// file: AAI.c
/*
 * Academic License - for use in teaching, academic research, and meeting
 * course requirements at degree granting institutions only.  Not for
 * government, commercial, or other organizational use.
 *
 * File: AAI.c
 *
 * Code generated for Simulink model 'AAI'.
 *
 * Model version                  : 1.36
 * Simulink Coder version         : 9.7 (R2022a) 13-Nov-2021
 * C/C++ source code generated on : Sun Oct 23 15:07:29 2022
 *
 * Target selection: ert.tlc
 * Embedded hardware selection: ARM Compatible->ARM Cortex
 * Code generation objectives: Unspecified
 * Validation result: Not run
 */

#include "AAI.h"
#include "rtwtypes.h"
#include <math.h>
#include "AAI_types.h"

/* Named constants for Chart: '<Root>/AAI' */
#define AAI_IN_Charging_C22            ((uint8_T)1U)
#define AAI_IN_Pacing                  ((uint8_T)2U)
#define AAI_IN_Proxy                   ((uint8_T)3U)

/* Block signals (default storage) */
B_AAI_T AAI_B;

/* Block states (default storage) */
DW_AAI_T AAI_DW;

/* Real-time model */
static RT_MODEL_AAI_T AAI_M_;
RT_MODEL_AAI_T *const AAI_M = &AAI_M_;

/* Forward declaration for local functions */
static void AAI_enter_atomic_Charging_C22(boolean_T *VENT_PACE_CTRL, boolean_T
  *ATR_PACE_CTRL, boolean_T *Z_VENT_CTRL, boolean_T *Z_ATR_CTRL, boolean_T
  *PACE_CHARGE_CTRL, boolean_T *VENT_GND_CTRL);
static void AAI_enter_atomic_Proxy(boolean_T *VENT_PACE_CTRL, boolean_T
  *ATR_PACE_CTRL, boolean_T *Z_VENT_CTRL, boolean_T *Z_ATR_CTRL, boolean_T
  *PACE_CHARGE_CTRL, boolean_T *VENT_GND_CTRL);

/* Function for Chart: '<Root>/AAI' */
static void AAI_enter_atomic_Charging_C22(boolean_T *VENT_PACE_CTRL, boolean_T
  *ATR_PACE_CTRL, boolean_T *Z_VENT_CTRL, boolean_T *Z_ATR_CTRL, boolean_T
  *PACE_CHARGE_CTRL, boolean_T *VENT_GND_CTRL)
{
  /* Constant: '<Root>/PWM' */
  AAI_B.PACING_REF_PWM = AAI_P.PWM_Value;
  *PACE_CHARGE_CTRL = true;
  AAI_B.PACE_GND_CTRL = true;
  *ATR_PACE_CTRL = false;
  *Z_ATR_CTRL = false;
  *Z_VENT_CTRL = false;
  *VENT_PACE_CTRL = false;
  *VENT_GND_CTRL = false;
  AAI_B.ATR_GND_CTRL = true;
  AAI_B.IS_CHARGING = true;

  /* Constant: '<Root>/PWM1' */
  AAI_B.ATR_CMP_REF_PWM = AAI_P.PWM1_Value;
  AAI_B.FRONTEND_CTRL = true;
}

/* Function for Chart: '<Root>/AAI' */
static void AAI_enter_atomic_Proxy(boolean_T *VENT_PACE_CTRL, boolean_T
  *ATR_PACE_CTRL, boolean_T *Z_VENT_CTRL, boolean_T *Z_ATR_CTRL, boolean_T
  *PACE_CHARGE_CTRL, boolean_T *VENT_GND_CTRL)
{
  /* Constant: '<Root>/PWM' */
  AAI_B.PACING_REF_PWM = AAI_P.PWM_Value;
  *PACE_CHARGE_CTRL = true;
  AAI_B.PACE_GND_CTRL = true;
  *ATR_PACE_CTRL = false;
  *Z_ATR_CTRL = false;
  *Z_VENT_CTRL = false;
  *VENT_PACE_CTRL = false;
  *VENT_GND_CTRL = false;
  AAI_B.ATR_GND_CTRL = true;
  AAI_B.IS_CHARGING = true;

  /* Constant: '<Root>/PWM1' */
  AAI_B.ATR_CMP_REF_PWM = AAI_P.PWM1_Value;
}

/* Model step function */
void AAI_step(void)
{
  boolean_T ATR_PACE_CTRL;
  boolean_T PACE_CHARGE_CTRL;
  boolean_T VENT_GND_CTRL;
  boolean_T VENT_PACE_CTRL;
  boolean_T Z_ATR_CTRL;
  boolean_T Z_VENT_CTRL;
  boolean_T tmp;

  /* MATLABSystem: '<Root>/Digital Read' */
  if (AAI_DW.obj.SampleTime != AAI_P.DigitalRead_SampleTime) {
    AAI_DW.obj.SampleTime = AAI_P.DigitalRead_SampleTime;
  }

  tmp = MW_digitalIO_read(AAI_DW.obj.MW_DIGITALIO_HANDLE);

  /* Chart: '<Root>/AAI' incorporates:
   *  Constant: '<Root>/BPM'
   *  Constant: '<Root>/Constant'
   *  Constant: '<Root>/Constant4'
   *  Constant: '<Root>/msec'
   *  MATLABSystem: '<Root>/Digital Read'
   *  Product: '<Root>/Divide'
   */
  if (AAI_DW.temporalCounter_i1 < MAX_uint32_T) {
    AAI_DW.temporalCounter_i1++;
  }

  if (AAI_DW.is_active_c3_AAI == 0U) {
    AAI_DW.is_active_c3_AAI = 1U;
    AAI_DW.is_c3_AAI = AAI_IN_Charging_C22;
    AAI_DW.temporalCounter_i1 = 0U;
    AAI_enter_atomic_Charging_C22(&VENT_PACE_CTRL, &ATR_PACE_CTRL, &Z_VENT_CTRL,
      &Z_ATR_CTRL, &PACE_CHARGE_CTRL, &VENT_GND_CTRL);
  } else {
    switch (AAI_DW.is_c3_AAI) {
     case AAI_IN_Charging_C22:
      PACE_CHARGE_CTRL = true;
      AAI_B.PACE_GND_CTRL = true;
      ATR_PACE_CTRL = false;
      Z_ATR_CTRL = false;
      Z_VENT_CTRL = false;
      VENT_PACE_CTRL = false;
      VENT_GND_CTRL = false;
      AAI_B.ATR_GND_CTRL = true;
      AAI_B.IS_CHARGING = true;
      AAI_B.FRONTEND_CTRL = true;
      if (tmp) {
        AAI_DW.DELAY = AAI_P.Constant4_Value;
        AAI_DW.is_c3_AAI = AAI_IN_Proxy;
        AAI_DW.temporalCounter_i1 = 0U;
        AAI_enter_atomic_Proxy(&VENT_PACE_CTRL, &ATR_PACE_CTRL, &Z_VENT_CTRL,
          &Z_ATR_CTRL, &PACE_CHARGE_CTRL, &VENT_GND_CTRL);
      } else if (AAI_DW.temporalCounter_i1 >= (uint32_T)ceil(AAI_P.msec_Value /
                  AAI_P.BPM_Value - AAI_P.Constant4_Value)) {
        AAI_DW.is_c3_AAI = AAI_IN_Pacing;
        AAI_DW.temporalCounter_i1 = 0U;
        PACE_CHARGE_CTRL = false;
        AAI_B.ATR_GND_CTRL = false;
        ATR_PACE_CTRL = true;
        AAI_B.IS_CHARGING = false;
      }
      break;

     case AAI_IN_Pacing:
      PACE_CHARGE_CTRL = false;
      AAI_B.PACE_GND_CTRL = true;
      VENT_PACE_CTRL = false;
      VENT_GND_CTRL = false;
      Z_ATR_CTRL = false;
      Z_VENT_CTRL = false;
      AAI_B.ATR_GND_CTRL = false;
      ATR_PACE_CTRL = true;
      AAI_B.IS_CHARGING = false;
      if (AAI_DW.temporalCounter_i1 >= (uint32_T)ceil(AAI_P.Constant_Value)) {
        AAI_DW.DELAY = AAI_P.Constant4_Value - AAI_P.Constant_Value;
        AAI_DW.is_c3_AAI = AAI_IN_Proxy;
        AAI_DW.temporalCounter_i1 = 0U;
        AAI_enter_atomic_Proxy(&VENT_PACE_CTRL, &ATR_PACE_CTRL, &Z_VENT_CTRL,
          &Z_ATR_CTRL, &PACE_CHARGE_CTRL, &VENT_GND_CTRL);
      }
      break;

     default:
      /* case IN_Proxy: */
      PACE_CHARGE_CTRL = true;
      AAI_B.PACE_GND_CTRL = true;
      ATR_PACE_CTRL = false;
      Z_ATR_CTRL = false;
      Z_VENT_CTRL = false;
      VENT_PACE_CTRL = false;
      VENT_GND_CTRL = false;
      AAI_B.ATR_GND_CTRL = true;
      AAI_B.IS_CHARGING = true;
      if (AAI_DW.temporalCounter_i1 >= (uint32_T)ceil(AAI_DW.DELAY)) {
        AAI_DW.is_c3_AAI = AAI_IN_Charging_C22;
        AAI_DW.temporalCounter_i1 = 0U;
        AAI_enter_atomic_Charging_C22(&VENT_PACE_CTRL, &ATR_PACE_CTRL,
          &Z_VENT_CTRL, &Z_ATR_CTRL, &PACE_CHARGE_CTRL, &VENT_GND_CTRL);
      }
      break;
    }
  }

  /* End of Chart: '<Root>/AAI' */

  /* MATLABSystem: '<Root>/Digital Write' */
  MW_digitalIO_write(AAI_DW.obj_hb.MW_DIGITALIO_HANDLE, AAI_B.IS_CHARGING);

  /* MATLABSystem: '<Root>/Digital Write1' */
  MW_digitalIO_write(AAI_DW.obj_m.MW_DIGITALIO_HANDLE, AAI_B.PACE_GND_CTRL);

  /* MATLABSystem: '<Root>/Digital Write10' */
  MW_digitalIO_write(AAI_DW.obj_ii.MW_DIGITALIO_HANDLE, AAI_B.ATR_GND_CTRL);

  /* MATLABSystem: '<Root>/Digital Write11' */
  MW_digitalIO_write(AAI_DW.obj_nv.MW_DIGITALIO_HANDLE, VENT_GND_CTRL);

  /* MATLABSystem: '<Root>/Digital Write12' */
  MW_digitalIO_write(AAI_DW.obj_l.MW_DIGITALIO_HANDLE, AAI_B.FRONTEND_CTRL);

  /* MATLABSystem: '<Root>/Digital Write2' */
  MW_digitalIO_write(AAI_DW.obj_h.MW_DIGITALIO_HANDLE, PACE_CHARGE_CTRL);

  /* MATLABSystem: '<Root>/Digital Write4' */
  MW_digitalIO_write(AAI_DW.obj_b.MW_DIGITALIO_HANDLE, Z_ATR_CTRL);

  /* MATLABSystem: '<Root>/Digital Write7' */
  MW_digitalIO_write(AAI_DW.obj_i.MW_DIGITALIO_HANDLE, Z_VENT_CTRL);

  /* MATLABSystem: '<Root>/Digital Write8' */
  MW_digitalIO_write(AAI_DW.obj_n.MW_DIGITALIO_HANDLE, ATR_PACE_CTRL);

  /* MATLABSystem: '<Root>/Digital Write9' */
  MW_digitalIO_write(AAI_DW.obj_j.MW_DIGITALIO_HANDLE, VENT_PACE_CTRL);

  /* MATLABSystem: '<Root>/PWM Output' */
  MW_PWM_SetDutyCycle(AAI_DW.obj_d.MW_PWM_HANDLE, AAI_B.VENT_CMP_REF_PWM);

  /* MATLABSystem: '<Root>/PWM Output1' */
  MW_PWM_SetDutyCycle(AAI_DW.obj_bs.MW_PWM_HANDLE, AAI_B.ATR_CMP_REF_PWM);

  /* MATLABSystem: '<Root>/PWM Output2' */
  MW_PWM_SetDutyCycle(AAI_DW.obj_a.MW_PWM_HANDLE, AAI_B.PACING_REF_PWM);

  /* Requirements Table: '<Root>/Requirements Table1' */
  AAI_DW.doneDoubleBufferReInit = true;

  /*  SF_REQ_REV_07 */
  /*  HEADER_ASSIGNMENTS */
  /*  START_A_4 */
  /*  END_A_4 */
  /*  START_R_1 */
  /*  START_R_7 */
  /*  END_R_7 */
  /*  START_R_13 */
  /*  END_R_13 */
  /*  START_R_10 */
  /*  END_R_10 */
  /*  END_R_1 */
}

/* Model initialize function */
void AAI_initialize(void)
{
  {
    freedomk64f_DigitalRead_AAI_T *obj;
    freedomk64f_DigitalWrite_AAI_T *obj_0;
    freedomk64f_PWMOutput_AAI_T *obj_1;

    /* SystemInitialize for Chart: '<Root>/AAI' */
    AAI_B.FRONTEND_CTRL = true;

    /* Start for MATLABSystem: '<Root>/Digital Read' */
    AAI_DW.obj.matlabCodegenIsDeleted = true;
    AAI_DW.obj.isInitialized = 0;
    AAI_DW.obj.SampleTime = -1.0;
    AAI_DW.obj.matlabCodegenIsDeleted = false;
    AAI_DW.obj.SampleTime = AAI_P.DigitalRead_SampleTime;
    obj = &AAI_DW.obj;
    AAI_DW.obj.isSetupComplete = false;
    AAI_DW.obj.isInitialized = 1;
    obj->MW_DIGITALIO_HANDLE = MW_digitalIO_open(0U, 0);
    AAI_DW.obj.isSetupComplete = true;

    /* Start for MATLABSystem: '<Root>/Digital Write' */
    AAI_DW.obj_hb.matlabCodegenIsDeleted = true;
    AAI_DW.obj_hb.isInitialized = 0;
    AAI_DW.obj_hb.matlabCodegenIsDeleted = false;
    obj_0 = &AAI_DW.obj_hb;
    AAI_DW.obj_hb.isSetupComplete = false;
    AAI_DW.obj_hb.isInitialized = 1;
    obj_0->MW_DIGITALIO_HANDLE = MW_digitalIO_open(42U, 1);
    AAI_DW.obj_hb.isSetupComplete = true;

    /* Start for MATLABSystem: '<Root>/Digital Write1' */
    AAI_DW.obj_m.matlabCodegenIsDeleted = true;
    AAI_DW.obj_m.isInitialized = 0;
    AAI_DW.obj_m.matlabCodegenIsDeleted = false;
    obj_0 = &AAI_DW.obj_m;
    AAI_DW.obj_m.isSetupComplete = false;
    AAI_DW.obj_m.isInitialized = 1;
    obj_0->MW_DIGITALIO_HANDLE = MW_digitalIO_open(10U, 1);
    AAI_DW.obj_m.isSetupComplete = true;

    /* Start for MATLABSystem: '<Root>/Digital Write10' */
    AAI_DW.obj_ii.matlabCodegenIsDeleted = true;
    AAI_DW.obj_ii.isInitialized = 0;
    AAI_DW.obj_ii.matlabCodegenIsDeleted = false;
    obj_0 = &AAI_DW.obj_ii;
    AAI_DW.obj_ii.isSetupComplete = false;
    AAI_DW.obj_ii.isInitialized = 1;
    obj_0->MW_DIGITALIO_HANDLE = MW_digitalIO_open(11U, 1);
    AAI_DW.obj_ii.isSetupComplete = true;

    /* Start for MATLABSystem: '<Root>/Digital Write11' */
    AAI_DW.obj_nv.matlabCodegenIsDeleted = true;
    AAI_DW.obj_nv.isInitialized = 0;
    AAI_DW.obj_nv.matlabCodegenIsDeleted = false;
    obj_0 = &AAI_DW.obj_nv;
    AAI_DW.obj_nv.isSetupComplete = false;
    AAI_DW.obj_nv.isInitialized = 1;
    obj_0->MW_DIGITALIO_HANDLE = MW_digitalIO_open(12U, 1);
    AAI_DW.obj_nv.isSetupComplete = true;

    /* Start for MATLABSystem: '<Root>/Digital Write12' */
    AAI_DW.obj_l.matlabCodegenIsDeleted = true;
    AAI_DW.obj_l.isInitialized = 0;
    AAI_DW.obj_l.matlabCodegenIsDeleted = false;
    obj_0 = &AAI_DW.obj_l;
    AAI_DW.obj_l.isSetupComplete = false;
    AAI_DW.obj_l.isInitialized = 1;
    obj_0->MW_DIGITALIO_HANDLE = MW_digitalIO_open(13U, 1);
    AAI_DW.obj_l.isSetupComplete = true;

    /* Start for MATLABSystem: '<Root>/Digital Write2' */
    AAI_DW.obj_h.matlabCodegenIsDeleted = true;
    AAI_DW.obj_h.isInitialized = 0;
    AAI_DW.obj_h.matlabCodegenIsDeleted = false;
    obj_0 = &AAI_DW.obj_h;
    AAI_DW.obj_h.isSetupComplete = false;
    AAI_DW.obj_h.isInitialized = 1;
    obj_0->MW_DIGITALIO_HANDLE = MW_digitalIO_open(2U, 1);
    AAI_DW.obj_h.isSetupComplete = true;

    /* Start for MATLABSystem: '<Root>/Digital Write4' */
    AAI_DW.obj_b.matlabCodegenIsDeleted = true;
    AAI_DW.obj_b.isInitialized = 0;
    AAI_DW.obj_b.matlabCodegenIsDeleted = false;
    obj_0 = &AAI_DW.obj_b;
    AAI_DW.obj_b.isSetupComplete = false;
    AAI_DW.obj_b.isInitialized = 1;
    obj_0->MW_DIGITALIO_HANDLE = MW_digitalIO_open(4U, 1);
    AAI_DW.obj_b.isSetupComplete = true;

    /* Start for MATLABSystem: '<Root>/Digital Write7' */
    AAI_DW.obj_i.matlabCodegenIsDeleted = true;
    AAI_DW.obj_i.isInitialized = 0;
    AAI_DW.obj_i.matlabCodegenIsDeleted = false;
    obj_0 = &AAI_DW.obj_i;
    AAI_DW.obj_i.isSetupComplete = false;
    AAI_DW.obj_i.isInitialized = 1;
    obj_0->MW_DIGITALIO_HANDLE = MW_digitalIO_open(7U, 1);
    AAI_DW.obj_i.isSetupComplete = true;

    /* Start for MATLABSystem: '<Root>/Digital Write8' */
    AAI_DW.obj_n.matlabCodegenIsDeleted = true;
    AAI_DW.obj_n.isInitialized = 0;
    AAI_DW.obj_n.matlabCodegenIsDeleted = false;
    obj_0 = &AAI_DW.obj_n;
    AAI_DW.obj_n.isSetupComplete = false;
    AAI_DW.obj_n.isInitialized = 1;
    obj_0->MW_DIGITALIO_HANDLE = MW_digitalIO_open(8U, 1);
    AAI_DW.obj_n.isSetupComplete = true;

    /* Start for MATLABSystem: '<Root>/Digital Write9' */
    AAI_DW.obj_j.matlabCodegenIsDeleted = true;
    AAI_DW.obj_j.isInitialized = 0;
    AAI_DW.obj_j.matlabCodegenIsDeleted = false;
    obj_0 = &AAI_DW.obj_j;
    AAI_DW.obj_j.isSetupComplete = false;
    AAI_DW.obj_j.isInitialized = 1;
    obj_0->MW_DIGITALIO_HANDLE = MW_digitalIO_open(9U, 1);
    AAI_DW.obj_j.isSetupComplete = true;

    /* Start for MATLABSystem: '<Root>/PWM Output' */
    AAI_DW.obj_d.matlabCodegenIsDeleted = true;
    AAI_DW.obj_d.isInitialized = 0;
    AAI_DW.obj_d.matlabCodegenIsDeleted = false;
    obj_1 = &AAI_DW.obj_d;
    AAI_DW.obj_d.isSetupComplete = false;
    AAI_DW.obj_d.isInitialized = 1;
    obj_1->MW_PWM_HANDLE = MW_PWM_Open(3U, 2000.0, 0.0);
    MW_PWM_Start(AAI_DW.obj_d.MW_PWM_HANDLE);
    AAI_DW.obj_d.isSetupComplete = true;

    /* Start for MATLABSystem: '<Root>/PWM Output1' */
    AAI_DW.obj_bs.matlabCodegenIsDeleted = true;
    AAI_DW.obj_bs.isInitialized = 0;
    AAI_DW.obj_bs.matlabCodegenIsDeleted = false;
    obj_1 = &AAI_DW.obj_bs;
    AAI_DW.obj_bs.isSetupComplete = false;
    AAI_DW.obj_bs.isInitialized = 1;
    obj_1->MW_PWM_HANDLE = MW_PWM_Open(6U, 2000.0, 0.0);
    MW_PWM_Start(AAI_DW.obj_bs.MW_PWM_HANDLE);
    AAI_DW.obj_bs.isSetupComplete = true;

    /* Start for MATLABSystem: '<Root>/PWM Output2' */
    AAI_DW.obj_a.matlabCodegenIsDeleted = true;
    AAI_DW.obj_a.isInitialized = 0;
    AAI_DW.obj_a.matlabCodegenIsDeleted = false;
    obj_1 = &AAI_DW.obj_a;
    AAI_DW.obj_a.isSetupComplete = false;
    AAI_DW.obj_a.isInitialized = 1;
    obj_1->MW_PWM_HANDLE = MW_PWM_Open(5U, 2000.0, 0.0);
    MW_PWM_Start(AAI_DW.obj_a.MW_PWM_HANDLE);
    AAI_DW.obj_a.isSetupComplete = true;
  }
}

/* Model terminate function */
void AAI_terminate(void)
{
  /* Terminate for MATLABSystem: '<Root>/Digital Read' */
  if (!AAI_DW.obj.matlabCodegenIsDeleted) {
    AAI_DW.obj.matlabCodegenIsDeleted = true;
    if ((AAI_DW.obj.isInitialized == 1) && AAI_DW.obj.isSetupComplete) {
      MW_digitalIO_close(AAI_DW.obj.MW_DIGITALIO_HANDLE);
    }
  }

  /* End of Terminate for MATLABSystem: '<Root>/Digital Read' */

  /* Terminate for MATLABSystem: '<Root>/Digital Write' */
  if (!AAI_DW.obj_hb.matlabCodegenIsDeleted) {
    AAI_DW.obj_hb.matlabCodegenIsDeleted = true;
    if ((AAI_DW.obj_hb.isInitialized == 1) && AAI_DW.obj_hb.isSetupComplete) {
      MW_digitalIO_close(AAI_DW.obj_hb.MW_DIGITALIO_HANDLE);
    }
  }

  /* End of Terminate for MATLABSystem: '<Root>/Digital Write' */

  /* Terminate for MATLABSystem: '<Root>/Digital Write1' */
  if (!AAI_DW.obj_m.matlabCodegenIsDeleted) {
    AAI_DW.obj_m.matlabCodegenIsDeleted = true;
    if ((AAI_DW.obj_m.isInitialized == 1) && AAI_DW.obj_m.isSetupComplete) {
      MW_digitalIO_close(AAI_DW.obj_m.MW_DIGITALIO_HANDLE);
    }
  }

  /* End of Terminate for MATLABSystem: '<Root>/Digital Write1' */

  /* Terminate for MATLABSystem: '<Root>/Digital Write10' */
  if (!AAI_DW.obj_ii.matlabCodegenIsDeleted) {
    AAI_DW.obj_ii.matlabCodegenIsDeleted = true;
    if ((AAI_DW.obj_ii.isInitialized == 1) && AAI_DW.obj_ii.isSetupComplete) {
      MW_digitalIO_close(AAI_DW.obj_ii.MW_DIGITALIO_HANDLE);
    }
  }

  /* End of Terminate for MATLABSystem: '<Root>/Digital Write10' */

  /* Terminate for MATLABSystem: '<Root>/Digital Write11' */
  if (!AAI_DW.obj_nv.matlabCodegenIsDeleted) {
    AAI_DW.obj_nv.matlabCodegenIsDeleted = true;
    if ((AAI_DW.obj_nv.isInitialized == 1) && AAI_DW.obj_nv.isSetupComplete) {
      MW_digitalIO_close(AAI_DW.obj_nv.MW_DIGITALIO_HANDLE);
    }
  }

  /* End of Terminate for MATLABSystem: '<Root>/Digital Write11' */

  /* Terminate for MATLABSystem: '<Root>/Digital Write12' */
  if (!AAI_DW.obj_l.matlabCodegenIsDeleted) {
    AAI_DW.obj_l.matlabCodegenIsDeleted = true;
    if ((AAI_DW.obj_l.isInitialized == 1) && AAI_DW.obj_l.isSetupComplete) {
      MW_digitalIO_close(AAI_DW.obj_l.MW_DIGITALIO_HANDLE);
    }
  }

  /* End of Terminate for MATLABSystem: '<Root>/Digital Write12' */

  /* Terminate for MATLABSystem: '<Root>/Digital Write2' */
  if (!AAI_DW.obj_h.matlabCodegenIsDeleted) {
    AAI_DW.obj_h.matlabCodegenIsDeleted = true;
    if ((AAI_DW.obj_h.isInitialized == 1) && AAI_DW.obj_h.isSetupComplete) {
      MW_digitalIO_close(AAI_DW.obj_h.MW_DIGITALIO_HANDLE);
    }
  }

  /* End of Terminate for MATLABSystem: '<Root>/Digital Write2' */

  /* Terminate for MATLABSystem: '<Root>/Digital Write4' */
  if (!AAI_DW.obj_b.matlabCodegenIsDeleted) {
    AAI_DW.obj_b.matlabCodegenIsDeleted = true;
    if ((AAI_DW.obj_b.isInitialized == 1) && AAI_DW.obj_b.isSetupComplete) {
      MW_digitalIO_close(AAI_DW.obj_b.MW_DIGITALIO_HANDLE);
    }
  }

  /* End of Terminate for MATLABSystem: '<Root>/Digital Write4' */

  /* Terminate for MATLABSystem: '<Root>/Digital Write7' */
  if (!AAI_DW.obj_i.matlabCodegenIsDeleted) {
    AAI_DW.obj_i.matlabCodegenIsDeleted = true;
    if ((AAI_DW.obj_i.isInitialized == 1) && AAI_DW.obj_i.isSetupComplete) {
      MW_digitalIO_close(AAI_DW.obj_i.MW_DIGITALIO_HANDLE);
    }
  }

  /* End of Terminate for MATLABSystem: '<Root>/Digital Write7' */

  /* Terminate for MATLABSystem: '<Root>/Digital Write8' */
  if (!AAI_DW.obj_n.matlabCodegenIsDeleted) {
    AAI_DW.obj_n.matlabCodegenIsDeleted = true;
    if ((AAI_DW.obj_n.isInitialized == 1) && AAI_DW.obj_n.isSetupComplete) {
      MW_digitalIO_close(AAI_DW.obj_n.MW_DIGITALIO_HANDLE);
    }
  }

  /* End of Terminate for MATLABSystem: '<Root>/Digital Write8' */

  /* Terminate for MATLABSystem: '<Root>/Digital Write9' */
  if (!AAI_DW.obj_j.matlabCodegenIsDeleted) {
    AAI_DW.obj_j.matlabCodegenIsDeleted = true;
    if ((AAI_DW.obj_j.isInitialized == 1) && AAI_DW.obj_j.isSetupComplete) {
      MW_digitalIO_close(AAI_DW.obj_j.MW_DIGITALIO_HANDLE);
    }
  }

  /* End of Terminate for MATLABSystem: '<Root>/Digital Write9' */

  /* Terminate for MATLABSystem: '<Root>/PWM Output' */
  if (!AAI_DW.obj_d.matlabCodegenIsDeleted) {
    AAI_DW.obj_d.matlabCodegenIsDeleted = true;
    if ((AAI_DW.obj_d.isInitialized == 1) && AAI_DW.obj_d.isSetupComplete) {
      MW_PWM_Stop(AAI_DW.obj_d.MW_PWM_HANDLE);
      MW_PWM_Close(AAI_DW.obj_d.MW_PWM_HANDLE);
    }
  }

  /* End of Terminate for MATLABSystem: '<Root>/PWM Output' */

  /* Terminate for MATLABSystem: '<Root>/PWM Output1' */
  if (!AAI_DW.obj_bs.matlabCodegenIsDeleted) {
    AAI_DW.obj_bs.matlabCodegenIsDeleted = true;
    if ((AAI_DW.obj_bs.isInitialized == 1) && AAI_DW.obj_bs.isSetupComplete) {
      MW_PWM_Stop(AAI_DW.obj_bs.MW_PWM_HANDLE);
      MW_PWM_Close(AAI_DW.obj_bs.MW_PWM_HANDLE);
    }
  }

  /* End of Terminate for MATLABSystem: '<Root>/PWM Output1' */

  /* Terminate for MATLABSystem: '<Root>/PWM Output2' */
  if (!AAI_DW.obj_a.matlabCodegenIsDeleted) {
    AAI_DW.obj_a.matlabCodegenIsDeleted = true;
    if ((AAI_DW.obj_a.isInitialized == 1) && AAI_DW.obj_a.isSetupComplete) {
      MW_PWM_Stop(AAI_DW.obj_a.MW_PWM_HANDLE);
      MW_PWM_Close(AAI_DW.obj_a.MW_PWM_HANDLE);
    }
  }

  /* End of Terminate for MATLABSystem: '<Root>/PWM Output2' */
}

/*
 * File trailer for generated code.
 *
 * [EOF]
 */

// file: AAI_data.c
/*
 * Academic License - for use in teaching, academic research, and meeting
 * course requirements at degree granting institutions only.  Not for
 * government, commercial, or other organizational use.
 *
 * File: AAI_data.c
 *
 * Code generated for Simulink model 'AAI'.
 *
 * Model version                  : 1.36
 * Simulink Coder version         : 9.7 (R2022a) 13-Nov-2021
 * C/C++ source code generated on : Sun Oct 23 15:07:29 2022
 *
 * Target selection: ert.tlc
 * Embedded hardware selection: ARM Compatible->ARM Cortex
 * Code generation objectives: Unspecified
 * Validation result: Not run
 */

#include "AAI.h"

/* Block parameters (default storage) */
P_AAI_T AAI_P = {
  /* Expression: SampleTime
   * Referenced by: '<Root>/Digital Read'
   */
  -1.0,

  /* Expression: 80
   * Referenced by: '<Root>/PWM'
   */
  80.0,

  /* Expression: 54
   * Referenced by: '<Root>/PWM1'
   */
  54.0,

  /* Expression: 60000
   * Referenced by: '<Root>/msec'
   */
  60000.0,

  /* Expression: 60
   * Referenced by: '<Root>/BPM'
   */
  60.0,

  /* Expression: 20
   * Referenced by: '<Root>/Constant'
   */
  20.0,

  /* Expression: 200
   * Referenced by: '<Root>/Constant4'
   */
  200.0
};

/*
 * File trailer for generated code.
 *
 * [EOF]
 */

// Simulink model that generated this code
simulink model "AAI"  (R2022a)
settings: Solver=FixedStepAuto  StartTime=0.0  StopTime=10.0  FixedStep=1e-3  RelTol=1e-3  EnableMultiTasking=on
undefined symbols (not defined in the file): D0, D10, D11, D12, D13, D2, D3, D4, D5, D6, D7, D8, D9, PTA0, PTA1, PTA2, PTB23, PTB9, PTC16, PTC2, PTC3, PTC4, PTD0, PTD1, PTD2, PTD3
libraries: frdmk64flib x14

== system AAI ==
  AAI : Stateflow chart  TreatAsAtomicUnit=on
  BPM : Constant  Value=60
  Constant : Constant  Value=20
  Constant4 : Constant  Value=200
  Digital Read : frdmk64flib/Digital Read  Whichpin=PTC16 (D0)  SampleTime=-1
  Digital Write : frdmk64flib/Digital Write  Whichpin=RED_LED
  Digital Write1 : frdmk64flib/Digital Write  Whichpin=PTD0 (D10)
  Digital Write10 : frdmk64flib/Digital Write  Whichpin=PTD2 (D11)
  Digital Write11 : frdmk64flib/Digital Write  Whichpin=PTD3 (D12)
  Digital Write12 : frdmk64flib/Digital Write  Whichpin=PTD1 (D13)
  Digital Write2 : frdmk64flib/Digital Write  Whichpin=PTB9 (D2)
  Digital Write4 : frdmk64flib/Digital Write  Whichpin=PTB23 (D4)
  Digital Write7 : frdmk64flib/Digital Write  Whichpin=PTC3 (D7)
  Digital Write8 : frdmk64flib/Digital Write  Whichpin=PTA0 (D8)
  Digital Write9 : frdmk64flib/Digital Write  Whichpin=PTC4 (D9)
  Divide : Product  Inputs=*/
  PWM : Constant  Value=80
  PWM Output : frdmk64flib/PWM Output  Whichpin=PTA1 (D3)  InitialFrequency=2000  InitialDutyCycle=0
  PWM Output1 : frdmk64flib/PWM Output  Whichpin=PTC2 (D6)  InitialFrequency=2000  InitialDutyCycle=0
  PWM Output2 : frdmk64flib/PWM Output  Whichpin=PTA2 (D5)  InitialFrequency=2000  InitialDutyCycle=0
  PWM1 : Constant  Value=54
  Requirements Table1 : Requirements Table  TreatAsAtomicUnit=on
  msec : Constant  Value=60000
  wires:
  AAI/2(PACE_CHARGE_CTRL) -> Requirements Table1/1(PACE_CHARGE_CTRL), Digital Write2/1
  AAI/7(Z_VENT_CTRL) -> Requirements Table1/3(Z_VENT_CTRL), Digital Write7/1
  AAI/9(VENT_PACE_CTRL) -> Requirements Table1/5(VENT_PACE_CTRL), Digital Write9/1
  AAI/10(PACE_GND_CTRL) -> Requirements Table1/6(PACE_GND_CTRL), Digital Write1/1
  AAI/11(ATR_GND_CTRL) -> Requirements Table1/7(ATR_GND_CTRL), Digital Write10/1
  AAI/12(VENT_GND_CTRL) -> Requirements Table1/8(VENT_GND_CTRL), Digital Write11/1
  AAI/13(FRONTEND_CTRL) -> Requirements Table1/9(FRONTEND_CTRL), Digital Write12/1
  PWM/1 -> AAI/1(DUTY_CYCLE)
  Constant/1 -> AAI/4(PULSE_WIDTH)
  Divide/1 -> AAI/3(PULSE_PERIOD)
  msec/1 -> Divide/1
  BPM/1 -> Divide/2
  AAI/1(IS_CHARGING) -> Digital Write/1
  AAI/5(PACING_REF_PWM) -> PWM Output2/1
  Digital Read/1 -> AAI/5(ATR_CMP_DETECT)
  Constant4/1 -> AAI/6(REFRACTORY_PERIOD)
  AAI/3(VENT_CMP_REF_PWM) -> PWM Output/1
  AAI/6(ATR_CMP_REF_PWM) -> PWM Output1/1
  PWM1/1 -> AAI/2(ATR_DUTY_CYCLE)
  AAI/4(Z_ATR_CTRL) -> Requirements Table1/2(Z_ATR_CTRL), Digital Write4/1
  AAI/8(ATR_PACE_CTRL) -> Requirements Table1/4(ATR_PACE_CTRL), Digital Write8/1

== stateflow chart AAI/Requirements Table1 ==
  (default) -> (junction 1073743086)
  (junction 1073743086) -> (junction 1073743087) : {
      | % SF_REQ_REV_07
      | }
  (junction 1073743087) -> (junction 1073743089) : {
      | % HEADER_ASSIGNMENTS
      |
      | }
  (junction 1073743089) -> (junction 1073743091) : {
      | % START_A_4
      | }
  (junction 1073743091) -> (junction 1073743093) : {
      | }
  (junction 1073743093) -> (junction 1073743095)
  (junction 1073743095) -> (junction 1073743097) : {
      | }
  (junction 1073743097) -> (junction 1073743099) : {
      | % END_A_4
      | }
  (junction 1073743099) -> (junction 1073743101) : {
      | % START_R_1
      | }
  (junction 1073743101) -> (junction 1073743103) : {
      | }
  (junction 1073743103) -> (junction 1073743105) : {
      |
      |
      | }
  (junction 1073743105) -> (junction 1073743107) : {
      | }
  (junction 1073743107) -> (junction 1073743109) : {
      | % START_R_7
      | }
  (junction 1073743109) -> (junction 1073743111) : {
      | }
  (junction 1073743111) -> (junction 1073743113)
  (junction 1073743113) -> (junction 1073743115) [order 1] : [(((prev(PACE_CHARGE_CTRL)) == (1))) && (((prev(Z_ATR_CTRL)) == (0))) && (((prev(Z_VENT_CTRL)) == (0))) && (((prev(ATR_PACE_CTRL)) == (0))) && (((prev(VENT_PACE_CTRL)) == (0))) && (((prev(PACE_GND_CTRL)) == (1))) && (((prev(ATR_GND_CTRL)) == (1))) && (((prev(VENT_GND_CTRL)) == (0))) && (((prev(FRONTEND_CTRL)) == (1)))]
  (junction 1073743113) -> (junction 1073743121) [order 2]
  (junction 1073743115) -> (junction 1073743117) : {
      | reqtable_postcondition((((PACE_CHARGE_CTRL) == (1))) && (((Z_ATR_CTRL) == (0))) && (((Z_VENT_CTRL) == (0))) && (((ATR_PACE_CTRL) == (0))) && (((VENT_PACE_CTRL) == (0))) && (((PACE_GND_CTRL) == (1))) && (((ATR_GND_CTRL) == (1))) && (((VENT_GND_CTRL) == (0))) && (((FRONTEND_CTRL) == (1))), 'R:1.1');
      |
      |
      | }
  (junction 1073743117) -> (junction 1073743119) : {
      | }
  (junction 1073743119) -> (junction 1073743121)
  (junction 1073743121) -> (junction 1073743123)
  (junction 1073743123) -> (junction 1073743125) : {
      | % END_R_7
      | }
  (junction 1073743125) -> (junction 1073743170) : {
      | % START_R_13
      | }
  (junction 1073743170) -> (junction 1073743172) : {
      | }
  (junction 1073743172) -> (junction 1073743174)
  (junction 1073743174) -> (junction 1073743176) [order 1] : [(((prev(PACE_CHARGE_CTRL)) == (1))) && (((prev(Z_ATR_CTRL)) == (0))) && (((prev(Z_VENT_CTRL)) == (0))) && (((prev(ATR_PACE_CTRL)) == (0))) && (((prev(VENT_PACE_CTRL)) == (0))) && (((prev(PACE_GND_CTRL)) == (1))) && (((prev(ATR_GND_CTRL)) == (1))) && (((prev(VENT_GND_CTRL)) == (0))) && (((prev(FRONTEND_CTRL)) == (1)))]
  (junction 1073743174) -> (junction 1073743182) [order 2]
  (junction 1073743176) -> (junction 1073743178) : {
      | reqtable_postcondition((((PACE_CHARGE_CTRL) == (1))) && (((Z_ATR_CTRL) == (0))) && (((Z_VENT_CTRL) == (0))) && (((ATR_PACE_CTRL) == (0))) && (((VENT_PACE_CTRL) == (0))) && (((PACE_GND_CTRL) == (1))) && (((ATR_GND_CTRL) == (1))) && (((VENT_GND_CTRL) == (0))) && (((FRONTEND_CTRL) == (1))), 'R:1.2');
      |
      |
      | }
  (junction 1073743178) -> (junction 1073743180) : {
      | }
  (junction 1073743180) -> (junction 1073743182)
  (junction 1073743182) -> (junction 1073743184)
  (junction 1073743184) -> (junction 1073743186) : {
      | % END_R_13
      | }
  (junction 1073743186) -> (junction 1073743127) : {
      | % START_R_10
      | }
  (junction 1073743127) -> (junction 1073743129) : {
      | }
  (junction 1073743129) -> (junction 1073743131)
  (junction 1073743131) -> (junction 1073743133) [order 1] : [(((prev(PACE_CHARGE_CTRL)) == (0))) && (((prev(Z_ATR_CTRL)) == (0))) && (((prev(Z_VENT_CTRL)) == (0))) && (((prev(ATR_PACE_CTRL)) == (1))) && (((prev(VENT_PACE_CTRL)) == (0))) && (((prev(PACE_GND_CTRL)) == (1))) && (((prev(ATR_GND_CTRL)) == (0))) && (((prev(VENT_GND_CTRL)) == (0))) && (((prev(FRONTEND_CTRL)) == (1)))]
  (junction 1073743131) -> (junction 1073743139) [order 2]
  (junction 1073743133) -> (junction 1073743135) : {
      | reqtable_postcondition((((PACE_CHARGE_CTRL) == (0))) && (((Z_ATR_CTRL) == (0))) && (((Z_VENT_CTRL) == (0))) && (((ATR_PACE_CTRL) == (1))) && (((VENT_PACE_CTRL) == (0))) && (((PACE_GND_CTRL) == (1))) && (((ATR_GND_CTRL) == (0))) && (((VENT_GND_CTRL) == (0))) && (((FRONTEND_CTRL) == (1))), 'R:1.3');
      |
      |
      | }
  (junction 1073743135) -> (junction 1073743137) : {
      | }
  (junction 1073743137) -> (junction 1073743139)
  (junction 1073743139) -> (junction 1073743141)
  (junction 1073743141) -> (junction 1073743161) : {
      | % END_R_10
      | }
  (junction 1073743161) -> (junction 1073743163) : {
      | % END_R_1
      | }
  data: PACE_CHARGE_CTRL input boolean; Z_ATR_CTRL input boolean; Z_VENT_CTRL input boolean; ATR_PACE_CTRL input boolean; VENT_PACE_CTRL input boolean; PACE_GND_CTRL input boolean; ATR_GND_CTRL input boolean; VENT_GND_CTRL input boolean; FRONTEND_CTRL input boolean =true

== stateflow chart AAI/AAI ==
  state Charging_C22
    entry:
    PACING_REF_PWM = DUTY_CYCLE
    PACE_CHARGE_CTRL = true
    PACE_GND_CTRL = true
    ATR_PACE_CTRL = false
    Z_ATR_CTRL = false
    Z_VENT_CTRL = false
    VENT_PACE_CTRL = false
    VENT_GND_CTRL = false
    ATR_GND_CTRL = true
    % For LED testing
    IS_CHARGING = true
    ATR_CMP_REF_PWM = ATR_DUTY_CYCLE
    FRONTEND_CTRL = true
  state Proxy
    entry:
    PACING_REF_PWM = DUTY_CYCLE
    PACE_CHARGE_CTRL = true
    PACE_GND_CTRL = true
    ATR_PACE_CTRL = false
    Z_ATR_CTRL = false
    Z_VENT_CTRL = false
    VENT_PACE_CTRL = false
    VENT_GND_CTRL = false
    ATR_GND_CTRL = true
    % For LED testing
    IS_CHARGING = true
    ATR_CMP_REF_PWM = ATR_DUTY_CYCLE
  state Pacing
    entry:
    PACE_CHARGE_CTRL = false
    PACE_GND_CTRL = true
    VENT_PACE_CTRL = false
    VENT_GND_CTRL = false
    Z_ATR_CTRL = false
    Z_VENT_CTRL = false
    ATR_GND_CTRL = false
    ATR_PACE_CTRL = true
    % For LED testing
    IS_CHARGING = false
  (default) -> Charging_C22
  Charging_C22 -> Proxy [order 1] : [ATR_CMP_DETECT ==  true]{DELAY = REFRACTORY_PERIOD}
  Proxy -> Charging_C22 : [after(DELAY,msec)]
  Charging_C22 -> Pacing [order 2] : [after(PULSE_PERIOD-REFRACTORY_PERIOD,msec)]
  Pacing -> Proxy : [after(PULSE_WIDTH,msec)]{DELAY = REFRACTORY_PERIOD - PULSE_WIDTH }
  data: IS_CHARGING output; PACE_CHARGE_CTRL output; VENT_CMP_REF_PWM output =0; Z_ATR_CTRL output; PACING_REF_PWM output; ATR_CMP_REF_PWM output =0; Z_VENT_CTRL output; ATR_PACE_CTRL output; VENT_PACE_CTRL output; PACE_GND_CTRL output; ATR_GND_CTRL output; VENT_GND_CTRL output; FRONTEND_CTRL output =true; DUTY_CYCLE input; ATR_DUTY_CYCLE input; PULSE_PERIOD input; PULSE_WIDTH input; ATR_CMP_DETECT input; DELAY local; REFRACTORY_PERIOD input
